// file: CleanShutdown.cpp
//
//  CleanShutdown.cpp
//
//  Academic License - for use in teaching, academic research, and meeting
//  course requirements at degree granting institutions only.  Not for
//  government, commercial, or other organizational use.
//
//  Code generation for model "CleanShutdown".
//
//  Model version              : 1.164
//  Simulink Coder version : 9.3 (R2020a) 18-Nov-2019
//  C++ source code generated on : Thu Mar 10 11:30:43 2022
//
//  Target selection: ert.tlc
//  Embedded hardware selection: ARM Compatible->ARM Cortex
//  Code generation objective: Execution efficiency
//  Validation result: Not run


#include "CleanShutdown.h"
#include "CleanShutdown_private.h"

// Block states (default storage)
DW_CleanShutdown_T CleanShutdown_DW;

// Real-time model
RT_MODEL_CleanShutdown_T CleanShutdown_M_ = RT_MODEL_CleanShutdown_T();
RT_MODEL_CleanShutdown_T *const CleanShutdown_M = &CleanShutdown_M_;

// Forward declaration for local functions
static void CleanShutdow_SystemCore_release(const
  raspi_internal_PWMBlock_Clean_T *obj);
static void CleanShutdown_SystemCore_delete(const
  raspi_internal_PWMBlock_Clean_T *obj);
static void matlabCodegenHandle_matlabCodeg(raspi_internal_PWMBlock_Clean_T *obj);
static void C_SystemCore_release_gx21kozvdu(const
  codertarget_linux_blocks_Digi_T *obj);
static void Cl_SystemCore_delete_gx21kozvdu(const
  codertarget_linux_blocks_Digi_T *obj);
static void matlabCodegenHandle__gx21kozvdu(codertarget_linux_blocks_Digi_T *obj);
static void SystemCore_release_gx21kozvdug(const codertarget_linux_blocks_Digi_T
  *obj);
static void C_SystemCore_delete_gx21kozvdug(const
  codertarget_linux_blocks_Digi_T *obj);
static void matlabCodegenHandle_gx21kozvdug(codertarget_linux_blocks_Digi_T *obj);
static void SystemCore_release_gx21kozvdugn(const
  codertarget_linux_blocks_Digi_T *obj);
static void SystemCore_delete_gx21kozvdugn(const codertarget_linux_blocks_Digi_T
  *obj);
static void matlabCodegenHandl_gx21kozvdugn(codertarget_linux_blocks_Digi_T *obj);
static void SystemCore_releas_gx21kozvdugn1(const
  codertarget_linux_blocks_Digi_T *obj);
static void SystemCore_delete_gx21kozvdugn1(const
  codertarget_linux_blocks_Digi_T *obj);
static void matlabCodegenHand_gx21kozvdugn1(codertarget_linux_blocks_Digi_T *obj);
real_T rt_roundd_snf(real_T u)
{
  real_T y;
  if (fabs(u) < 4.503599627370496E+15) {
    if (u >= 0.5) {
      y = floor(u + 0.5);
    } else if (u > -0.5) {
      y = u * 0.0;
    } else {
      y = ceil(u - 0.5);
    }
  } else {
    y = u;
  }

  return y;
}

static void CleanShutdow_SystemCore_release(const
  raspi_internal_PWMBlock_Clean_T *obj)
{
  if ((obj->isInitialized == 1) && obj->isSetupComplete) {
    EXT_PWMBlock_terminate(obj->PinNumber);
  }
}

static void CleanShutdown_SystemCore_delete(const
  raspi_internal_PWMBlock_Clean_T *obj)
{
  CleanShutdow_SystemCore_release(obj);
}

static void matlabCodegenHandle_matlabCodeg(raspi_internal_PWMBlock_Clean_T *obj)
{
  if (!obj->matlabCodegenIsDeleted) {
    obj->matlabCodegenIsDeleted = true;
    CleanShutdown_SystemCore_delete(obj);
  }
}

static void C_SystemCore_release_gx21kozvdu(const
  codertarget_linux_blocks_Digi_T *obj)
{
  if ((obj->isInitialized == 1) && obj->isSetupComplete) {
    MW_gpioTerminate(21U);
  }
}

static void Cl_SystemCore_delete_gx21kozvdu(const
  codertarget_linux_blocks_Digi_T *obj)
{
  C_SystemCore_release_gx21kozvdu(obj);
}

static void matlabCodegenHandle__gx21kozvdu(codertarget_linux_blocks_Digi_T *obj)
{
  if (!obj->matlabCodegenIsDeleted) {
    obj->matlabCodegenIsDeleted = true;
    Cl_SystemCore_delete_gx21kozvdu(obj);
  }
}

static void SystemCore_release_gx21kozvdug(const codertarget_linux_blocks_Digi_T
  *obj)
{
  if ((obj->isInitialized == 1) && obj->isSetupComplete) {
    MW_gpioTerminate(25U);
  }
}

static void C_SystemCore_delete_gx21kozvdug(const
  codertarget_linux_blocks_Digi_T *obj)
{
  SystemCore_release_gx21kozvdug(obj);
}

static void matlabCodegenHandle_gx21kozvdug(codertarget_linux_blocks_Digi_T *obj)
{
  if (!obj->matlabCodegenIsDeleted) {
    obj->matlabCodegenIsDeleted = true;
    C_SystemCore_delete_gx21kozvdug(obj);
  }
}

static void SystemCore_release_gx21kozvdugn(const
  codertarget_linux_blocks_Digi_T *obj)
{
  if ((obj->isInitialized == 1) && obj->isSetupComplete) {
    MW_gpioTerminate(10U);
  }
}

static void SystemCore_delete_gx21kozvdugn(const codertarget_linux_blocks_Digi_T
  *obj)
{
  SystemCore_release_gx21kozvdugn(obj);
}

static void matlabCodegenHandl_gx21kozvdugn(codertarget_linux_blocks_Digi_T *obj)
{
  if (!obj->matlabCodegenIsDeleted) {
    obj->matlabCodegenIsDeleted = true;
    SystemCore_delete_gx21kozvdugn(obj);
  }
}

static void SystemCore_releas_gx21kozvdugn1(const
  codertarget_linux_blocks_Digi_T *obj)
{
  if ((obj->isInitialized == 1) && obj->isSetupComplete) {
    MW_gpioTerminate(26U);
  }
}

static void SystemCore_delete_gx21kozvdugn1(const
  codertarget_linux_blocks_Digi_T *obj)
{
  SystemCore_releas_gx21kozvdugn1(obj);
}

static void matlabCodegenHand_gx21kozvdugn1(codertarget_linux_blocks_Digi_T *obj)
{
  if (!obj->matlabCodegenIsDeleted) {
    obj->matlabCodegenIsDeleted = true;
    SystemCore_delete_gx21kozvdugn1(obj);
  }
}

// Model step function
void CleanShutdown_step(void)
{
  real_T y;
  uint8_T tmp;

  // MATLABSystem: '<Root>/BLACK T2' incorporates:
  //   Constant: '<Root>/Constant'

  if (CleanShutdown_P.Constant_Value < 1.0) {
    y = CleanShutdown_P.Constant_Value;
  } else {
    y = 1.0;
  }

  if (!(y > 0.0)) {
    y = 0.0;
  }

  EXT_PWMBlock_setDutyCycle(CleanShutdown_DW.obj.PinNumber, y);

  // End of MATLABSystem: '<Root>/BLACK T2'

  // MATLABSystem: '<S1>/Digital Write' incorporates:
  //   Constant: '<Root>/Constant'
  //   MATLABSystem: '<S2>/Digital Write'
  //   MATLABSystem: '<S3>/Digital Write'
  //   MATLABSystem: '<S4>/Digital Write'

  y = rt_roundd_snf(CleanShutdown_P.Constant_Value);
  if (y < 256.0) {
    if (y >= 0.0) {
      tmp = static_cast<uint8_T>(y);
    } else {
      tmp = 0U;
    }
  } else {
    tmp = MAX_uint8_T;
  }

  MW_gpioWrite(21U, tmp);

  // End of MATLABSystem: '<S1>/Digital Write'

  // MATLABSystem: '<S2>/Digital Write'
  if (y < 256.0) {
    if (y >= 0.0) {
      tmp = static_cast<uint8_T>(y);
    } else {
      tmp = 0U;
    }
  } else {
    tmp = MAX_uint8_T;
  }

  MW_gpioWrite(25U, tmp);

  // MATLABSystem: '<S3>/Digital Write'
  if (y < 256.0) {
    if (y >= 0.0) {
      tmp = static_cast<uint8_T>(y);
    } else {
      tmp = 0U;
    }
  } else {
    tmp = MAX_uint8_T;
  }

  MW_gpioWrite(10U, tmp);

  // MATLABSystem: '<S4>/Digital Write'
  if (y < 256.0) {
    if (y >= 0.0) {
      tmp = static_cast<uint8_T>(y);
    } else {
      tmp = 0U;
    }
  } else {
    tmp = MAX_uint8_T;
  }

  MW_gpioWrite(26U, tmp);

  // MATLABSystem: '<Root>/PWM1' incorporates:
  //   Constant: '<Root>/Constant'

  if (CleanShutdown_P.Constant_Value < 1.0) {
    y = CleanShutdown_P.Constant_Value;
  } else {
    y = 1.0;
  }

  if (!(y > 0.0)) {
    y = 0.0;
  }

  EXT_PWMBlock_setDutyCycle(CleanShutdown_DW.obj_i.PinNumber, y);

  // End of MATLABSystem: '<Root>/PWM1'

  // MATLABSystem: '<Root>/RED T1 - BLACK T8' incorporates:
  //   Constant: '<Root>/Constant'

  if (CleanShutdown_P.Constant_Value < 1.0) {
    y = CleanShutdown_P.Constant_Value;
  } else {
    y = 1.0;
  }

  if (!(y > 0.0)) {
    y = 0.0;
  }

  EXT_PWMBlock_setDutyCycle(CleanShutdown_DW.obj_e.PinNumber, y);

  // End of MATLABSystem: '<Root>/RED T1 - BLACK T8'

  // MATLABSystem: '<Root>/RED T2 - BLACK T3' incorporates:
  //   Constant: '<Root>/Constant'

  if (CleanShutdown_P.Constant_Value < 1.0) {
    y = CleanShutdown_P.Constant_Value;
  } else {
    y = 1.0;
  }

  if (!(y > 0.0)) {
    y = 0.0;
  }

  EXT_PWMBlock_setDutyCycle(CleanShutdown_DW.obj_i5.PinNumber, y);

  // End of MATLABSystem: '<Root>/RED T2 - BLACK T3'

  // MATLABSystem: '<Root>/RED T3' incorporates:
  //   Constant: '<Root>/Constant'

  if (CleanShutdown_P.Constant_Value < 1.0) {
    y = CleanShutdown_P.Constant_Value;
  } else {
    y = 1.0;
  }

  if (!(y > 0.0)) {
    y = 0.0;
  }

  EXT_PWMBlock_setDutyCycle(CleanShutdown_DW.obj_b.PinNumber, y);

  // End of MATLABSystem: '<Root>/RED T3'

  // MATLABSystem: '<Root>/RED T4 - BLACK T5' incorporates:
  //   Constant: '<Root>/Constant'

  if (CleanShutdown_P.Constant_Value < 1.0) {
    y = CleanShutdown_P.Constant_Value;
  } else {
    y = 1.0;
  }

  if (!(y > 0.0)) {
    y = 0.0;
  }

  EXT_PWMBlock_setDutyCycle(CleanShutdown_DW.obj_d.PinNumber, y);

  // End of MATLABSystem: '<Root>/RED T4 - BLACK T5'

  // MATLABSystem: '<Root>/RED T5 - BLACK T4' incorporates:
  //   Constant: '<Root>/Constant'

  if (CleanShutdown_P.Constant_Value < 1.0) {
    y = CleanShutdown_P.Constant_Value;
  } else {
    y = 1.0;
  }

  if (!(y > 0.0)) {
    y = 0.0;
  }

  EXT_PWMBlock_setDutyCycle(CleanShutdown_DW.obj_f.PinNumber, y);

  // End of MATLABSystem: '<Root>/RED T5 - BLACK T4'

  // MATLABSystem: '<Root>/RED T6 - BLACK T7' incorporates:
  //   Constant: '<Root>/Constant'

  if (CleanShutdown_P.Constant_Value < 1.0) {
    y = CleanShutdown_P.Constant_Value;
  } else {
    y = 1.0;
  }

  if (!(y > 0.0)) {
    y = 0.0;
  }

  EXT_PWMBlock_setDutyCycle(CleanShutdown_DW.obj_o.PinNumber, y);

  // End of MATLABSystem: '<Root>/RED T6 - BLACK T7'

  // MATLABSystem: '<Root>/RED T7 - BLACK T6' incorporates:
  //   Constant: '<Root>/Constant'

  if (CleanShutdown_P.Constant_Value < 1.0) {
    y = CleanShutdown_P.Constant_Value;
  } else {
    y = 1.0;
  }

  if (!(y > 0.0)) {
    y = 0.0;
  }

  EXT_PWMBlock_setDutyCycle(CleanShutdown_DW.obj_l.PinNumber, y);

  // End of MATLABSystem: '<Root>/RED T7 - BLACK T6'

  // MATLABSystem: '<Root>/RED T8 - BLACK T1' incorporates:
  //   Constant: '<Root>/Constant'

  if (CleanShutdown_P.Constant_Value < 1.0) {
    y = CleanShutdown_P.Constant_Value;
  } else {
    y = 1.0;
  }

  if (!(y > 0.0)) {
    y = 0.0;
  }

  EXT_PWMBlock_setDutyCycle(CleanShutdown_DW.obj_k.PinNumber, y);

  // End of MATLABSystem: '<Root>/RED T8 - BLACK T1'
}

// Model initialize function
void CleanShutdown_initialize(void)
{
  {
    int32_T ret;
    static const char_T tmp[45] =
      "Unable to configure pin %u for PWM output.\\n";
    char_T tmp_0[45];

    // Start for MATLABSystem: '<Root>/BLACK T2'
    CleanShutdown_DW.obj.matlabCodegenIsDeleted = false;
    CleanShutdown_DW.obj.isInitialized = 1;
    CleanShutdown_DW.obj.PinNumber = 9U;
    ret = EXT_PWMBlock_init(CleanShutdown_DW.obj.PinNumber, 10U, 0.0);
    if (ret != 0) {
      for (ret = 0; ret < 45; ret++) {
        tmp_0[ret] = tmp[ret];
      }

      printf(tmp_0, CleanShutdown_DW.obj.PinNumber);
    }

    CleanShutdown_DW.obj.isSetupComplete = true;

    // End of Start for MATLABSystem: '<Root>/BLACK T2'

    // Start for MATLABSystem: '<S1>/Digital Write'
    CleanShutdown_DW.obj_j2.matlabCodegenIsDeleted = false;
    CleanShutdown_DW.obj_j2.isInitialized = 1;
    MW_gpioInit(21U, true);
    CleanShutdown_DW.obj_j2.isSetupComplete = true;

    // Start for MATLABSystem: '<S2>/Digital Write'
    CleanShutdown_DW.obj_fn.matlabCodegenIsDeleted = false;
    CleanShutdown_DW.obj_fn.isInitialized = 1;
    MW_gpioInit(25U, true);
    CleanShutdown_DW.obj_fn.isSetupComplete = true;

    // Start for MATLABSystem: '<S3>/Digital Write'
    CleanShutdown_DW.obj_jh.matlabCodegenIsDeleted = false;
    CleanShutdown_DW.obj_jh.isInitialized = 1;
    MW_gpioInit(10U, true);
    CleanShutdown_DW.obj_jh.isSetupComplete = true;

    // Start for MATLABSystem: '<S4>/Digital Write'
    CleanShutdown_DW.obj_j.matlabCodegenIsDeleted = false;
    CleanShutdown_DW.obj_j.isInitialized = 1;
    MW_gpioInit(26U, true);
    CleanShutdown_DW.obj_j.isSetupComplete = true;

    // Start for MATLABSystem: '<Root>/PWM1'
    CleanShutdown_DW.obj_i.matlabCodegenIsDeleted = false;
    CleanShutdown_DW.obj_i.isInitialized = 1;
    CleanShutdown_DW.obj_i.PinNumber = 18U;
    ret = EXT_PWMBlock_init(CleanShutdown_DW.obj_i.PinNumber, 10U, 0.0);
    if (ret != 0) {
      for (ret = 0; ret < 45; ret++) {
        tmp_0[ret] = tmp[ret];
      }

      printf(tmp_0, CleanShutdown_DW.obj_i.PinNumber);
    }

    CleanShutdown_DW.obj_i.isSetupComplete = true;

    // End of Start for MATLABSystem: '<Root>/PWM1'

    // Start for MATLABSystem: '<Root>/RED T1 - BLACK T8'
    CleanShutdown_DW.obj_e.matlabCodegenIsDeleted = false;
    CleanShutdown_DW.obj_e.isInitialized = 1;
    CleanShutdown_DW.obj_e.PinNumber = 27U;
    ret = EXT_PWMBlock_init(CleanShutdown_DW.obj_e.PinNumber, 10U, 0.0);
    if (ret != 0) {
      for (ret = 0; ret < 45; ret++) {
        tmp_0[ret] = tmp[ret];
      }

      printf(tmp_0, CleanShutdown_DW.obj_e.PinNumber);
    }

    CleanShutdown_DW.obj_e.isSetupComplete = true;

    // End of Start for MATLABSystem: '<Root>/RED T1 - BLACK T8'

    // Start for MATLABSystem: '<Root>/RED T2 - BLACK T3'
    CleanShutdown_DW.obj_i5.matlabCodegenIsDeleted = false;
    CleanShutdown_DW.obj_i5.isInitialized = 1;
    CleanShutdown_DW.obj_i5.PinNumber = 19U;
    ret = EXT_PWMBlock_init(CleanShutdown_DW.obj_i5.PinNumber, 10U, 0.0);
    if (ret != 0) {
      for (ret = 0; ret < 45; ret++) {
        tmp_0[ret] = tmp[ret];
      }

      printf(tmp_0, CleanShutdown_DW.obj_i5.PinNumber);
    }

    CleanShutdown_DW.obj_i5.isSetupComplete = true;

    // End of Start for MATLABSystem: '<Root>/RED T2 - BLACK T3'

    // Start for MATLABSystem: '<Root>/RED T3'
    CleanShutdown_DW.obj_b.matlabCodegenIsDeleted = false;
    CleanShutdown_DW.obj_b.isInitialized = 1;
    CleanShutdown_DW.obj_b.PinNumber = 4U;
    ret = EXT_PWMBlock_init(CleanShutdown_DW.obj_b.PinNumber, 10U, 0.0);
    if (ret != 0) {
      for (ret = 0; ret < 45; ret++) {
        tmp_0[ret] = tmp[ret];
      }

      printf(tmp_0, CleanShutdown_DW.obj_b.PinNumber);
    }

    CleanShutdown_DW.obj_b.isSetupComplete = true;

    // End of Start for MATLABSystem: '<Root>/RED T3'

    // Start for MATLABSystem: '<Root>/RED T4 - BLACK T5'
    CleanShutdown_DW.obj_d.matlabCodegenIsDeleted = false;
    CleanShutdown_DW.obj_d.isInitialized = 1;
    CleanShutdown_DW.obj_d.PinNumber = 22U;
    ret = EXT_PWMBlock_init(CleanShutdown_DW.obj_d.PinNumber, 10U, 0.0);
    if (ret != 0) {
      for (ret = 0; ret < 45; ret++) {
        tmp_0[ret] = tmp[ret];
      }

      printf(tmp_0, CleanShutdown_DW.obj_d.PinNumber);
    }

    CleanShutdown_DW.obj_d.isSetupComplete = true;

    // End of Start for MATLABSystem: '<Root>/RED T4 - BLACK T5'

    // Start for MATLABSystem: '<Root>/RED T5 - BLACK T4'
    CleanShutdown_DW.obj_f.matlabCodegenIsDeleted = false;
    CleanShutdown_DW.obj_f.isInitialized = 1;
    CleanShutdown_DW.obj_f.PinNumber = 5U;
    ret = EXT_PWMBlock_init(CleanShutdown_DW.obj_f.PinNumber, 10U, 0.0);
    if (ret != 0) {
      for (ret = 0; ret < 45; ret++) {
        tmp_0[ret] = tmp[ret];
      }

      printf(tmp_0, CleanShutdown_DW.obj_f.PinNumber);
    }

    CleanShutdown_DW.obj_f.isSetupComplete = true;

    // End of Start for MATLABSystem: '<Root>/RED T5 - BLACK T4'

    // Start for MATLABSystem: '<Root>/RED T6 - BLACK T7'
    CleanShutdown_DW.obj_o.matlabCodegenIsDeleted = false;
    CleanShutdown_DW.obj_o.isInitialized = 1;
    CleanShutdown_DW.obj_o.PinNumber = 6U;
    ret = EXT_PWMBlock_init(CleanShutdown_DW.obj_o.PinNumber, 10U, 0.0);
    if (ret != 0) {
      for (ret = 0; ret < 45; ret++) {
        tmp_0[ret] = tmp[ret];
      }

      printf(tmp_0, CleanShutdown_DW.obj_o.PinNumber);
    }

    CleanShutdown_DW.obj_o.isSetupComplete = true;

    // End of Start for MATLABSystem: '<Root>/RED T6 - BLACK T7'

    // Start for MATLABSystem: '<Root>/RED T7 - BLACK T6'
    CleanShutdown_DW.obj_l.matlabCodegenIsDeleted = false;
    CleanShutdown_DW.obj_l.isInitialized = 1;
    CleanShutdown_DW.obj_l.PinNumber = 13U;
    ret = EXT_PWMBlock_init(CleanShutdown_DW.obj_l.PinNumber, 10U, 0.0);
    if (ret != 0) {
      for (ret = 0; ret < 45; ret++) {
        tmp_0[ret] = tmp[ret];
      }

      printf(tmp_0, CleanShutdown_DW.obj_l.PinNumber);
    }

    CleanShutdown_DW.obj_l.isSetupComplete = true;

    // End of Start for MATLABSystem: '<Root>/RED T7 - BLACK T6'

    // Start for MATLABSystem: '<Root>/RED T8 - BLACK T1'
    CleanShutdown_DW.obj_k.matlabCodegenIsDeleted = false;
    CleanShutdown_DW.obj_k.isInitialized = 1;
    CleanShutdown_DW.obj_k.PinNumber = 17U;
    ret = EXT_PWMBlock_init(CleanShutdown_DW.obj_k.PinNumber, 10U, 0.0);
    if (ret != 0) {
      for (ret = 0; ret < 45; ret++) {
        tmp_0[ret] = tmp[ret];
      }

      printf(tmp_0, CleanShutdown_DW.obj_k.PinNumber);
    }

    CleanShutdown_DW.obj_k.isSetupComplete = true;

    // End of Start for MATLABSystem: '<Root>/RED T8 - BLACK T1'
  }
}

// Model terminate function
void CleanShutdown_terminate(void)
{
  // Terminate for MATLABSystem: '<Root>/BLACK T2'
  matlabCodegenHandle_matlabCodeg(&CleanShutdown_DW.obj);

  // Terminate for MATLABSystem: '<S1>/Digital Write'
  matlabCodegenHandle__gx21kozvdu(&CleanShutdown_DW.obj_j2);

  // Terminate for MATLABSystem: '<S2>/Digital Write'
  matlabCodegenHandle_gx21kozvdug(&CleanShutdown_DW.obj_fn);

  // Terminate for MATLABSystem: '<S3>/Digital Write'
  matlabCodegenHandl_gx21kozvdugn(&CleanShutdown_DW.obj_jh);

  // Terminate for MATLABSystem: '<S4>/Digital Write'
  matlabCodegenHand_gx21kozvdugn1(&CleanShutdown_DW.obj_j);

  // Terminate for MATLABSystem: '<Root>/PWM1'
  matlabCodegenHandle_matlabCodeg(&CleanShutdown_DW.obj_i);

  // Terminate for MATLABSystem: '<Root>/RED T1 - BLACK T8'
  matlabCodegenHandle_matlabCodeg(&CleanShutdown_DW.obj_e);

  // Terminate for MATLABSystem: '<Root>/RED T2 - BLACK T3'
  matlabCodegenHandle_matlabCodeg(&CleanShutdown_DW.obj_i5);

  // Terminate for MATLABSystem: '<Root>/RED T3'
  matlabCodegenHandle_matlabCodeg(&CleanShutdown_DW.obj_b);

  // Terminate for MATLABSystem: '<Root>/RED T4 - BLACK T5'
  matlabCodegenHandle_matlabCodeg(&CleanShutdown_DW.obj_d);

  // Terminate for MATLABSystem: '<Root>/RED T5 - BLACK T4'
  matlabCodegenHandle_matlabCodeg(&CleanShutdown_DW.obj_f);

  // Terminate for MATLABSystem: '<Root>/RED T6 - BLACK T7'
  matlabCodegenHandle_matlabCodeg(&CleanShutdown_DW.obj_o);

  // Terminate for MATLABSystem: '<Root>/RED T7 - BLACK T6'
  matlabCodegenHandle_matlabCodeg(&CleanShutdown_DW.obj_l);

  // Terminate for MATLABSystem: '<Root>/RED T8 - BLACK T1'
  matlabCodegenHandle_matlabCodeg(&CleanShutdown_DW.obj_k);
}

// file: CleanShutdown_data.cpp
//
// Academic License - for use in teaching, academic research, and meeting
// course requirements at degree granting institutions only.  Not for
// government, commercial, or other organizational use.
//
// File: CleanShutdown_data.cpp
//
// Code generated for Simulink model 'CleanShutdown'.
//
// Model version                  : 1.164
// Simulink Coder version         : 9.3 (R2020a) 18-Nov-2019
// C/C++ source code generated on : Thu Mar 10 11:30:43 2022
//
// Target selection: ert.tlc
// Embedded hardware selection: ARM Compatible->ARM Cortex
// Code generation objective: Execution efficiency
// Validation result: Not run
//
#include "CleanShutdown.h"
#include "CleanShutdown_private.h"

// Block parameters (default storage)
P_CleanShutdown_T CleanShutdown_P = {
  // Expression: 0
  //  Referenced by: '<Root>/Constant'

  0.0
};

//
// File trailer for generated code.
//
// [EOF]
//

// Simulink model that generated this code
simulink model "CleanShutdown"  (R2020a)
settings: Solver=FixedStepAuto  StartTime=0.0  StopTime=inf  FixedStep=baseRate  RelTol=1e-3  EnableMultiTasking=on
libraries: raspberrypiBasiclib x10, embdlinuxlib x4

== system CleanShutdown ==
  note: This code must be compiled on all platforms so that a clean shutdown is possible.
  note: Clean Shutdown - v3.05
  note: SPOT 3.0
      | Software Suite
  BLACK T2 : raspberrypiBasiclib/PWM  board=Pi 3 Model B  Pin_=9  Frequency=10  blockPlatform=Raspberry Pi
  Constant : Constant  Value=0
  GPIO Write : embdlinuxlib/GPIO Write  board=Pi 3 Model B  gpio=21  direction=Output  blockPlatform=Raspberry Pi
  GPIO Write1 : embdlinuxlib/GPIO Write  board=Pi 3 Model B  gpio=25  direction=Output  blockPlatform=Raspberry Pi
  GPIO for Magnet : embdlinuxlib/GPIO Write  board=Pi 3 Model B  gpio=10  direction=Output  blockPlatform=Raspberry Pi
  GPIO for Pucks : embdlinuxlib/GPIO Write  board=Pi 3 Model B  gpio=26  direction=Output  blockPlatform=Raspberry Pi
  PWM1 : raspberrypiBasiclib/PWM  board=Pi 3 Model B  Pin_=18  Frequency=10  blockPlatform=Raspberry Pi
  RED T1 - BLACK T8 : raspberrypiBasiclib/PWM  board=Pi 3 Model B  Pin_=27  Frequency=10  blockPlatform=Raspberry Pi
  RED T2 - BLACK T3 : raspberrypiBasiclib/PWM  board=Pi 3 Model B  Pin_=19  Frequency=10  blockPlatform=Raspberry Pi
  RED T3 : raspberrypiBasiclib/PWM  board=Pi 3 Model B  Pin_=4  Frequency=10  blockPlatform=Raspberry Pi
  RED T4 - BLACK T5 : raspberrypiBasiclib/PWM  board=Pi 3 Model B  Pin_=22  Frequency=10  blockPlatform=Raspberry Pi
  RED T5 - BLACK T4 : raspberrypiBasiclib/PWM  board=Pi 3 Model B  Pin_=5  Frequency=10  blockPlatform=Raspberry Pi
  RED T6 - BLACK T7 : raspberrypiBasiclib/PWM  board=Pi 3 Model B  Pin_=6  Frequency=10  blockPlatform=Raspberry Pi
  RED T7 - BLACK T6 : raspberrypiBasiclib/PWM  board=Pi 3 Model B  Pin_=13  Frequency=10  blockPlatform=Raspberry Pi
  RED T8 - BLACK T1 : raspberrypiBasiclib/PWM  board=Pi 3 Model B  Pin_=17  Frequency=10  blockPlatform=Raspberry Pi
  wires:
  Constant/1 -> PWM1/1, RED T6 - BLACK T7/1, RED T5 - BLACK T4/1, RED T4 - BLACK T5/1, BLACK T2/1, RED T3/1, RED T2 - BLACK T3/1, RED T1 - BLACK T8/1, GPIO Write/1, GPIO Write1/1, RED T8 - BLACK T1/1, RED T7 - BLACK T6/1, GPIO for Pucks/1, GPIO for Magnet/1
